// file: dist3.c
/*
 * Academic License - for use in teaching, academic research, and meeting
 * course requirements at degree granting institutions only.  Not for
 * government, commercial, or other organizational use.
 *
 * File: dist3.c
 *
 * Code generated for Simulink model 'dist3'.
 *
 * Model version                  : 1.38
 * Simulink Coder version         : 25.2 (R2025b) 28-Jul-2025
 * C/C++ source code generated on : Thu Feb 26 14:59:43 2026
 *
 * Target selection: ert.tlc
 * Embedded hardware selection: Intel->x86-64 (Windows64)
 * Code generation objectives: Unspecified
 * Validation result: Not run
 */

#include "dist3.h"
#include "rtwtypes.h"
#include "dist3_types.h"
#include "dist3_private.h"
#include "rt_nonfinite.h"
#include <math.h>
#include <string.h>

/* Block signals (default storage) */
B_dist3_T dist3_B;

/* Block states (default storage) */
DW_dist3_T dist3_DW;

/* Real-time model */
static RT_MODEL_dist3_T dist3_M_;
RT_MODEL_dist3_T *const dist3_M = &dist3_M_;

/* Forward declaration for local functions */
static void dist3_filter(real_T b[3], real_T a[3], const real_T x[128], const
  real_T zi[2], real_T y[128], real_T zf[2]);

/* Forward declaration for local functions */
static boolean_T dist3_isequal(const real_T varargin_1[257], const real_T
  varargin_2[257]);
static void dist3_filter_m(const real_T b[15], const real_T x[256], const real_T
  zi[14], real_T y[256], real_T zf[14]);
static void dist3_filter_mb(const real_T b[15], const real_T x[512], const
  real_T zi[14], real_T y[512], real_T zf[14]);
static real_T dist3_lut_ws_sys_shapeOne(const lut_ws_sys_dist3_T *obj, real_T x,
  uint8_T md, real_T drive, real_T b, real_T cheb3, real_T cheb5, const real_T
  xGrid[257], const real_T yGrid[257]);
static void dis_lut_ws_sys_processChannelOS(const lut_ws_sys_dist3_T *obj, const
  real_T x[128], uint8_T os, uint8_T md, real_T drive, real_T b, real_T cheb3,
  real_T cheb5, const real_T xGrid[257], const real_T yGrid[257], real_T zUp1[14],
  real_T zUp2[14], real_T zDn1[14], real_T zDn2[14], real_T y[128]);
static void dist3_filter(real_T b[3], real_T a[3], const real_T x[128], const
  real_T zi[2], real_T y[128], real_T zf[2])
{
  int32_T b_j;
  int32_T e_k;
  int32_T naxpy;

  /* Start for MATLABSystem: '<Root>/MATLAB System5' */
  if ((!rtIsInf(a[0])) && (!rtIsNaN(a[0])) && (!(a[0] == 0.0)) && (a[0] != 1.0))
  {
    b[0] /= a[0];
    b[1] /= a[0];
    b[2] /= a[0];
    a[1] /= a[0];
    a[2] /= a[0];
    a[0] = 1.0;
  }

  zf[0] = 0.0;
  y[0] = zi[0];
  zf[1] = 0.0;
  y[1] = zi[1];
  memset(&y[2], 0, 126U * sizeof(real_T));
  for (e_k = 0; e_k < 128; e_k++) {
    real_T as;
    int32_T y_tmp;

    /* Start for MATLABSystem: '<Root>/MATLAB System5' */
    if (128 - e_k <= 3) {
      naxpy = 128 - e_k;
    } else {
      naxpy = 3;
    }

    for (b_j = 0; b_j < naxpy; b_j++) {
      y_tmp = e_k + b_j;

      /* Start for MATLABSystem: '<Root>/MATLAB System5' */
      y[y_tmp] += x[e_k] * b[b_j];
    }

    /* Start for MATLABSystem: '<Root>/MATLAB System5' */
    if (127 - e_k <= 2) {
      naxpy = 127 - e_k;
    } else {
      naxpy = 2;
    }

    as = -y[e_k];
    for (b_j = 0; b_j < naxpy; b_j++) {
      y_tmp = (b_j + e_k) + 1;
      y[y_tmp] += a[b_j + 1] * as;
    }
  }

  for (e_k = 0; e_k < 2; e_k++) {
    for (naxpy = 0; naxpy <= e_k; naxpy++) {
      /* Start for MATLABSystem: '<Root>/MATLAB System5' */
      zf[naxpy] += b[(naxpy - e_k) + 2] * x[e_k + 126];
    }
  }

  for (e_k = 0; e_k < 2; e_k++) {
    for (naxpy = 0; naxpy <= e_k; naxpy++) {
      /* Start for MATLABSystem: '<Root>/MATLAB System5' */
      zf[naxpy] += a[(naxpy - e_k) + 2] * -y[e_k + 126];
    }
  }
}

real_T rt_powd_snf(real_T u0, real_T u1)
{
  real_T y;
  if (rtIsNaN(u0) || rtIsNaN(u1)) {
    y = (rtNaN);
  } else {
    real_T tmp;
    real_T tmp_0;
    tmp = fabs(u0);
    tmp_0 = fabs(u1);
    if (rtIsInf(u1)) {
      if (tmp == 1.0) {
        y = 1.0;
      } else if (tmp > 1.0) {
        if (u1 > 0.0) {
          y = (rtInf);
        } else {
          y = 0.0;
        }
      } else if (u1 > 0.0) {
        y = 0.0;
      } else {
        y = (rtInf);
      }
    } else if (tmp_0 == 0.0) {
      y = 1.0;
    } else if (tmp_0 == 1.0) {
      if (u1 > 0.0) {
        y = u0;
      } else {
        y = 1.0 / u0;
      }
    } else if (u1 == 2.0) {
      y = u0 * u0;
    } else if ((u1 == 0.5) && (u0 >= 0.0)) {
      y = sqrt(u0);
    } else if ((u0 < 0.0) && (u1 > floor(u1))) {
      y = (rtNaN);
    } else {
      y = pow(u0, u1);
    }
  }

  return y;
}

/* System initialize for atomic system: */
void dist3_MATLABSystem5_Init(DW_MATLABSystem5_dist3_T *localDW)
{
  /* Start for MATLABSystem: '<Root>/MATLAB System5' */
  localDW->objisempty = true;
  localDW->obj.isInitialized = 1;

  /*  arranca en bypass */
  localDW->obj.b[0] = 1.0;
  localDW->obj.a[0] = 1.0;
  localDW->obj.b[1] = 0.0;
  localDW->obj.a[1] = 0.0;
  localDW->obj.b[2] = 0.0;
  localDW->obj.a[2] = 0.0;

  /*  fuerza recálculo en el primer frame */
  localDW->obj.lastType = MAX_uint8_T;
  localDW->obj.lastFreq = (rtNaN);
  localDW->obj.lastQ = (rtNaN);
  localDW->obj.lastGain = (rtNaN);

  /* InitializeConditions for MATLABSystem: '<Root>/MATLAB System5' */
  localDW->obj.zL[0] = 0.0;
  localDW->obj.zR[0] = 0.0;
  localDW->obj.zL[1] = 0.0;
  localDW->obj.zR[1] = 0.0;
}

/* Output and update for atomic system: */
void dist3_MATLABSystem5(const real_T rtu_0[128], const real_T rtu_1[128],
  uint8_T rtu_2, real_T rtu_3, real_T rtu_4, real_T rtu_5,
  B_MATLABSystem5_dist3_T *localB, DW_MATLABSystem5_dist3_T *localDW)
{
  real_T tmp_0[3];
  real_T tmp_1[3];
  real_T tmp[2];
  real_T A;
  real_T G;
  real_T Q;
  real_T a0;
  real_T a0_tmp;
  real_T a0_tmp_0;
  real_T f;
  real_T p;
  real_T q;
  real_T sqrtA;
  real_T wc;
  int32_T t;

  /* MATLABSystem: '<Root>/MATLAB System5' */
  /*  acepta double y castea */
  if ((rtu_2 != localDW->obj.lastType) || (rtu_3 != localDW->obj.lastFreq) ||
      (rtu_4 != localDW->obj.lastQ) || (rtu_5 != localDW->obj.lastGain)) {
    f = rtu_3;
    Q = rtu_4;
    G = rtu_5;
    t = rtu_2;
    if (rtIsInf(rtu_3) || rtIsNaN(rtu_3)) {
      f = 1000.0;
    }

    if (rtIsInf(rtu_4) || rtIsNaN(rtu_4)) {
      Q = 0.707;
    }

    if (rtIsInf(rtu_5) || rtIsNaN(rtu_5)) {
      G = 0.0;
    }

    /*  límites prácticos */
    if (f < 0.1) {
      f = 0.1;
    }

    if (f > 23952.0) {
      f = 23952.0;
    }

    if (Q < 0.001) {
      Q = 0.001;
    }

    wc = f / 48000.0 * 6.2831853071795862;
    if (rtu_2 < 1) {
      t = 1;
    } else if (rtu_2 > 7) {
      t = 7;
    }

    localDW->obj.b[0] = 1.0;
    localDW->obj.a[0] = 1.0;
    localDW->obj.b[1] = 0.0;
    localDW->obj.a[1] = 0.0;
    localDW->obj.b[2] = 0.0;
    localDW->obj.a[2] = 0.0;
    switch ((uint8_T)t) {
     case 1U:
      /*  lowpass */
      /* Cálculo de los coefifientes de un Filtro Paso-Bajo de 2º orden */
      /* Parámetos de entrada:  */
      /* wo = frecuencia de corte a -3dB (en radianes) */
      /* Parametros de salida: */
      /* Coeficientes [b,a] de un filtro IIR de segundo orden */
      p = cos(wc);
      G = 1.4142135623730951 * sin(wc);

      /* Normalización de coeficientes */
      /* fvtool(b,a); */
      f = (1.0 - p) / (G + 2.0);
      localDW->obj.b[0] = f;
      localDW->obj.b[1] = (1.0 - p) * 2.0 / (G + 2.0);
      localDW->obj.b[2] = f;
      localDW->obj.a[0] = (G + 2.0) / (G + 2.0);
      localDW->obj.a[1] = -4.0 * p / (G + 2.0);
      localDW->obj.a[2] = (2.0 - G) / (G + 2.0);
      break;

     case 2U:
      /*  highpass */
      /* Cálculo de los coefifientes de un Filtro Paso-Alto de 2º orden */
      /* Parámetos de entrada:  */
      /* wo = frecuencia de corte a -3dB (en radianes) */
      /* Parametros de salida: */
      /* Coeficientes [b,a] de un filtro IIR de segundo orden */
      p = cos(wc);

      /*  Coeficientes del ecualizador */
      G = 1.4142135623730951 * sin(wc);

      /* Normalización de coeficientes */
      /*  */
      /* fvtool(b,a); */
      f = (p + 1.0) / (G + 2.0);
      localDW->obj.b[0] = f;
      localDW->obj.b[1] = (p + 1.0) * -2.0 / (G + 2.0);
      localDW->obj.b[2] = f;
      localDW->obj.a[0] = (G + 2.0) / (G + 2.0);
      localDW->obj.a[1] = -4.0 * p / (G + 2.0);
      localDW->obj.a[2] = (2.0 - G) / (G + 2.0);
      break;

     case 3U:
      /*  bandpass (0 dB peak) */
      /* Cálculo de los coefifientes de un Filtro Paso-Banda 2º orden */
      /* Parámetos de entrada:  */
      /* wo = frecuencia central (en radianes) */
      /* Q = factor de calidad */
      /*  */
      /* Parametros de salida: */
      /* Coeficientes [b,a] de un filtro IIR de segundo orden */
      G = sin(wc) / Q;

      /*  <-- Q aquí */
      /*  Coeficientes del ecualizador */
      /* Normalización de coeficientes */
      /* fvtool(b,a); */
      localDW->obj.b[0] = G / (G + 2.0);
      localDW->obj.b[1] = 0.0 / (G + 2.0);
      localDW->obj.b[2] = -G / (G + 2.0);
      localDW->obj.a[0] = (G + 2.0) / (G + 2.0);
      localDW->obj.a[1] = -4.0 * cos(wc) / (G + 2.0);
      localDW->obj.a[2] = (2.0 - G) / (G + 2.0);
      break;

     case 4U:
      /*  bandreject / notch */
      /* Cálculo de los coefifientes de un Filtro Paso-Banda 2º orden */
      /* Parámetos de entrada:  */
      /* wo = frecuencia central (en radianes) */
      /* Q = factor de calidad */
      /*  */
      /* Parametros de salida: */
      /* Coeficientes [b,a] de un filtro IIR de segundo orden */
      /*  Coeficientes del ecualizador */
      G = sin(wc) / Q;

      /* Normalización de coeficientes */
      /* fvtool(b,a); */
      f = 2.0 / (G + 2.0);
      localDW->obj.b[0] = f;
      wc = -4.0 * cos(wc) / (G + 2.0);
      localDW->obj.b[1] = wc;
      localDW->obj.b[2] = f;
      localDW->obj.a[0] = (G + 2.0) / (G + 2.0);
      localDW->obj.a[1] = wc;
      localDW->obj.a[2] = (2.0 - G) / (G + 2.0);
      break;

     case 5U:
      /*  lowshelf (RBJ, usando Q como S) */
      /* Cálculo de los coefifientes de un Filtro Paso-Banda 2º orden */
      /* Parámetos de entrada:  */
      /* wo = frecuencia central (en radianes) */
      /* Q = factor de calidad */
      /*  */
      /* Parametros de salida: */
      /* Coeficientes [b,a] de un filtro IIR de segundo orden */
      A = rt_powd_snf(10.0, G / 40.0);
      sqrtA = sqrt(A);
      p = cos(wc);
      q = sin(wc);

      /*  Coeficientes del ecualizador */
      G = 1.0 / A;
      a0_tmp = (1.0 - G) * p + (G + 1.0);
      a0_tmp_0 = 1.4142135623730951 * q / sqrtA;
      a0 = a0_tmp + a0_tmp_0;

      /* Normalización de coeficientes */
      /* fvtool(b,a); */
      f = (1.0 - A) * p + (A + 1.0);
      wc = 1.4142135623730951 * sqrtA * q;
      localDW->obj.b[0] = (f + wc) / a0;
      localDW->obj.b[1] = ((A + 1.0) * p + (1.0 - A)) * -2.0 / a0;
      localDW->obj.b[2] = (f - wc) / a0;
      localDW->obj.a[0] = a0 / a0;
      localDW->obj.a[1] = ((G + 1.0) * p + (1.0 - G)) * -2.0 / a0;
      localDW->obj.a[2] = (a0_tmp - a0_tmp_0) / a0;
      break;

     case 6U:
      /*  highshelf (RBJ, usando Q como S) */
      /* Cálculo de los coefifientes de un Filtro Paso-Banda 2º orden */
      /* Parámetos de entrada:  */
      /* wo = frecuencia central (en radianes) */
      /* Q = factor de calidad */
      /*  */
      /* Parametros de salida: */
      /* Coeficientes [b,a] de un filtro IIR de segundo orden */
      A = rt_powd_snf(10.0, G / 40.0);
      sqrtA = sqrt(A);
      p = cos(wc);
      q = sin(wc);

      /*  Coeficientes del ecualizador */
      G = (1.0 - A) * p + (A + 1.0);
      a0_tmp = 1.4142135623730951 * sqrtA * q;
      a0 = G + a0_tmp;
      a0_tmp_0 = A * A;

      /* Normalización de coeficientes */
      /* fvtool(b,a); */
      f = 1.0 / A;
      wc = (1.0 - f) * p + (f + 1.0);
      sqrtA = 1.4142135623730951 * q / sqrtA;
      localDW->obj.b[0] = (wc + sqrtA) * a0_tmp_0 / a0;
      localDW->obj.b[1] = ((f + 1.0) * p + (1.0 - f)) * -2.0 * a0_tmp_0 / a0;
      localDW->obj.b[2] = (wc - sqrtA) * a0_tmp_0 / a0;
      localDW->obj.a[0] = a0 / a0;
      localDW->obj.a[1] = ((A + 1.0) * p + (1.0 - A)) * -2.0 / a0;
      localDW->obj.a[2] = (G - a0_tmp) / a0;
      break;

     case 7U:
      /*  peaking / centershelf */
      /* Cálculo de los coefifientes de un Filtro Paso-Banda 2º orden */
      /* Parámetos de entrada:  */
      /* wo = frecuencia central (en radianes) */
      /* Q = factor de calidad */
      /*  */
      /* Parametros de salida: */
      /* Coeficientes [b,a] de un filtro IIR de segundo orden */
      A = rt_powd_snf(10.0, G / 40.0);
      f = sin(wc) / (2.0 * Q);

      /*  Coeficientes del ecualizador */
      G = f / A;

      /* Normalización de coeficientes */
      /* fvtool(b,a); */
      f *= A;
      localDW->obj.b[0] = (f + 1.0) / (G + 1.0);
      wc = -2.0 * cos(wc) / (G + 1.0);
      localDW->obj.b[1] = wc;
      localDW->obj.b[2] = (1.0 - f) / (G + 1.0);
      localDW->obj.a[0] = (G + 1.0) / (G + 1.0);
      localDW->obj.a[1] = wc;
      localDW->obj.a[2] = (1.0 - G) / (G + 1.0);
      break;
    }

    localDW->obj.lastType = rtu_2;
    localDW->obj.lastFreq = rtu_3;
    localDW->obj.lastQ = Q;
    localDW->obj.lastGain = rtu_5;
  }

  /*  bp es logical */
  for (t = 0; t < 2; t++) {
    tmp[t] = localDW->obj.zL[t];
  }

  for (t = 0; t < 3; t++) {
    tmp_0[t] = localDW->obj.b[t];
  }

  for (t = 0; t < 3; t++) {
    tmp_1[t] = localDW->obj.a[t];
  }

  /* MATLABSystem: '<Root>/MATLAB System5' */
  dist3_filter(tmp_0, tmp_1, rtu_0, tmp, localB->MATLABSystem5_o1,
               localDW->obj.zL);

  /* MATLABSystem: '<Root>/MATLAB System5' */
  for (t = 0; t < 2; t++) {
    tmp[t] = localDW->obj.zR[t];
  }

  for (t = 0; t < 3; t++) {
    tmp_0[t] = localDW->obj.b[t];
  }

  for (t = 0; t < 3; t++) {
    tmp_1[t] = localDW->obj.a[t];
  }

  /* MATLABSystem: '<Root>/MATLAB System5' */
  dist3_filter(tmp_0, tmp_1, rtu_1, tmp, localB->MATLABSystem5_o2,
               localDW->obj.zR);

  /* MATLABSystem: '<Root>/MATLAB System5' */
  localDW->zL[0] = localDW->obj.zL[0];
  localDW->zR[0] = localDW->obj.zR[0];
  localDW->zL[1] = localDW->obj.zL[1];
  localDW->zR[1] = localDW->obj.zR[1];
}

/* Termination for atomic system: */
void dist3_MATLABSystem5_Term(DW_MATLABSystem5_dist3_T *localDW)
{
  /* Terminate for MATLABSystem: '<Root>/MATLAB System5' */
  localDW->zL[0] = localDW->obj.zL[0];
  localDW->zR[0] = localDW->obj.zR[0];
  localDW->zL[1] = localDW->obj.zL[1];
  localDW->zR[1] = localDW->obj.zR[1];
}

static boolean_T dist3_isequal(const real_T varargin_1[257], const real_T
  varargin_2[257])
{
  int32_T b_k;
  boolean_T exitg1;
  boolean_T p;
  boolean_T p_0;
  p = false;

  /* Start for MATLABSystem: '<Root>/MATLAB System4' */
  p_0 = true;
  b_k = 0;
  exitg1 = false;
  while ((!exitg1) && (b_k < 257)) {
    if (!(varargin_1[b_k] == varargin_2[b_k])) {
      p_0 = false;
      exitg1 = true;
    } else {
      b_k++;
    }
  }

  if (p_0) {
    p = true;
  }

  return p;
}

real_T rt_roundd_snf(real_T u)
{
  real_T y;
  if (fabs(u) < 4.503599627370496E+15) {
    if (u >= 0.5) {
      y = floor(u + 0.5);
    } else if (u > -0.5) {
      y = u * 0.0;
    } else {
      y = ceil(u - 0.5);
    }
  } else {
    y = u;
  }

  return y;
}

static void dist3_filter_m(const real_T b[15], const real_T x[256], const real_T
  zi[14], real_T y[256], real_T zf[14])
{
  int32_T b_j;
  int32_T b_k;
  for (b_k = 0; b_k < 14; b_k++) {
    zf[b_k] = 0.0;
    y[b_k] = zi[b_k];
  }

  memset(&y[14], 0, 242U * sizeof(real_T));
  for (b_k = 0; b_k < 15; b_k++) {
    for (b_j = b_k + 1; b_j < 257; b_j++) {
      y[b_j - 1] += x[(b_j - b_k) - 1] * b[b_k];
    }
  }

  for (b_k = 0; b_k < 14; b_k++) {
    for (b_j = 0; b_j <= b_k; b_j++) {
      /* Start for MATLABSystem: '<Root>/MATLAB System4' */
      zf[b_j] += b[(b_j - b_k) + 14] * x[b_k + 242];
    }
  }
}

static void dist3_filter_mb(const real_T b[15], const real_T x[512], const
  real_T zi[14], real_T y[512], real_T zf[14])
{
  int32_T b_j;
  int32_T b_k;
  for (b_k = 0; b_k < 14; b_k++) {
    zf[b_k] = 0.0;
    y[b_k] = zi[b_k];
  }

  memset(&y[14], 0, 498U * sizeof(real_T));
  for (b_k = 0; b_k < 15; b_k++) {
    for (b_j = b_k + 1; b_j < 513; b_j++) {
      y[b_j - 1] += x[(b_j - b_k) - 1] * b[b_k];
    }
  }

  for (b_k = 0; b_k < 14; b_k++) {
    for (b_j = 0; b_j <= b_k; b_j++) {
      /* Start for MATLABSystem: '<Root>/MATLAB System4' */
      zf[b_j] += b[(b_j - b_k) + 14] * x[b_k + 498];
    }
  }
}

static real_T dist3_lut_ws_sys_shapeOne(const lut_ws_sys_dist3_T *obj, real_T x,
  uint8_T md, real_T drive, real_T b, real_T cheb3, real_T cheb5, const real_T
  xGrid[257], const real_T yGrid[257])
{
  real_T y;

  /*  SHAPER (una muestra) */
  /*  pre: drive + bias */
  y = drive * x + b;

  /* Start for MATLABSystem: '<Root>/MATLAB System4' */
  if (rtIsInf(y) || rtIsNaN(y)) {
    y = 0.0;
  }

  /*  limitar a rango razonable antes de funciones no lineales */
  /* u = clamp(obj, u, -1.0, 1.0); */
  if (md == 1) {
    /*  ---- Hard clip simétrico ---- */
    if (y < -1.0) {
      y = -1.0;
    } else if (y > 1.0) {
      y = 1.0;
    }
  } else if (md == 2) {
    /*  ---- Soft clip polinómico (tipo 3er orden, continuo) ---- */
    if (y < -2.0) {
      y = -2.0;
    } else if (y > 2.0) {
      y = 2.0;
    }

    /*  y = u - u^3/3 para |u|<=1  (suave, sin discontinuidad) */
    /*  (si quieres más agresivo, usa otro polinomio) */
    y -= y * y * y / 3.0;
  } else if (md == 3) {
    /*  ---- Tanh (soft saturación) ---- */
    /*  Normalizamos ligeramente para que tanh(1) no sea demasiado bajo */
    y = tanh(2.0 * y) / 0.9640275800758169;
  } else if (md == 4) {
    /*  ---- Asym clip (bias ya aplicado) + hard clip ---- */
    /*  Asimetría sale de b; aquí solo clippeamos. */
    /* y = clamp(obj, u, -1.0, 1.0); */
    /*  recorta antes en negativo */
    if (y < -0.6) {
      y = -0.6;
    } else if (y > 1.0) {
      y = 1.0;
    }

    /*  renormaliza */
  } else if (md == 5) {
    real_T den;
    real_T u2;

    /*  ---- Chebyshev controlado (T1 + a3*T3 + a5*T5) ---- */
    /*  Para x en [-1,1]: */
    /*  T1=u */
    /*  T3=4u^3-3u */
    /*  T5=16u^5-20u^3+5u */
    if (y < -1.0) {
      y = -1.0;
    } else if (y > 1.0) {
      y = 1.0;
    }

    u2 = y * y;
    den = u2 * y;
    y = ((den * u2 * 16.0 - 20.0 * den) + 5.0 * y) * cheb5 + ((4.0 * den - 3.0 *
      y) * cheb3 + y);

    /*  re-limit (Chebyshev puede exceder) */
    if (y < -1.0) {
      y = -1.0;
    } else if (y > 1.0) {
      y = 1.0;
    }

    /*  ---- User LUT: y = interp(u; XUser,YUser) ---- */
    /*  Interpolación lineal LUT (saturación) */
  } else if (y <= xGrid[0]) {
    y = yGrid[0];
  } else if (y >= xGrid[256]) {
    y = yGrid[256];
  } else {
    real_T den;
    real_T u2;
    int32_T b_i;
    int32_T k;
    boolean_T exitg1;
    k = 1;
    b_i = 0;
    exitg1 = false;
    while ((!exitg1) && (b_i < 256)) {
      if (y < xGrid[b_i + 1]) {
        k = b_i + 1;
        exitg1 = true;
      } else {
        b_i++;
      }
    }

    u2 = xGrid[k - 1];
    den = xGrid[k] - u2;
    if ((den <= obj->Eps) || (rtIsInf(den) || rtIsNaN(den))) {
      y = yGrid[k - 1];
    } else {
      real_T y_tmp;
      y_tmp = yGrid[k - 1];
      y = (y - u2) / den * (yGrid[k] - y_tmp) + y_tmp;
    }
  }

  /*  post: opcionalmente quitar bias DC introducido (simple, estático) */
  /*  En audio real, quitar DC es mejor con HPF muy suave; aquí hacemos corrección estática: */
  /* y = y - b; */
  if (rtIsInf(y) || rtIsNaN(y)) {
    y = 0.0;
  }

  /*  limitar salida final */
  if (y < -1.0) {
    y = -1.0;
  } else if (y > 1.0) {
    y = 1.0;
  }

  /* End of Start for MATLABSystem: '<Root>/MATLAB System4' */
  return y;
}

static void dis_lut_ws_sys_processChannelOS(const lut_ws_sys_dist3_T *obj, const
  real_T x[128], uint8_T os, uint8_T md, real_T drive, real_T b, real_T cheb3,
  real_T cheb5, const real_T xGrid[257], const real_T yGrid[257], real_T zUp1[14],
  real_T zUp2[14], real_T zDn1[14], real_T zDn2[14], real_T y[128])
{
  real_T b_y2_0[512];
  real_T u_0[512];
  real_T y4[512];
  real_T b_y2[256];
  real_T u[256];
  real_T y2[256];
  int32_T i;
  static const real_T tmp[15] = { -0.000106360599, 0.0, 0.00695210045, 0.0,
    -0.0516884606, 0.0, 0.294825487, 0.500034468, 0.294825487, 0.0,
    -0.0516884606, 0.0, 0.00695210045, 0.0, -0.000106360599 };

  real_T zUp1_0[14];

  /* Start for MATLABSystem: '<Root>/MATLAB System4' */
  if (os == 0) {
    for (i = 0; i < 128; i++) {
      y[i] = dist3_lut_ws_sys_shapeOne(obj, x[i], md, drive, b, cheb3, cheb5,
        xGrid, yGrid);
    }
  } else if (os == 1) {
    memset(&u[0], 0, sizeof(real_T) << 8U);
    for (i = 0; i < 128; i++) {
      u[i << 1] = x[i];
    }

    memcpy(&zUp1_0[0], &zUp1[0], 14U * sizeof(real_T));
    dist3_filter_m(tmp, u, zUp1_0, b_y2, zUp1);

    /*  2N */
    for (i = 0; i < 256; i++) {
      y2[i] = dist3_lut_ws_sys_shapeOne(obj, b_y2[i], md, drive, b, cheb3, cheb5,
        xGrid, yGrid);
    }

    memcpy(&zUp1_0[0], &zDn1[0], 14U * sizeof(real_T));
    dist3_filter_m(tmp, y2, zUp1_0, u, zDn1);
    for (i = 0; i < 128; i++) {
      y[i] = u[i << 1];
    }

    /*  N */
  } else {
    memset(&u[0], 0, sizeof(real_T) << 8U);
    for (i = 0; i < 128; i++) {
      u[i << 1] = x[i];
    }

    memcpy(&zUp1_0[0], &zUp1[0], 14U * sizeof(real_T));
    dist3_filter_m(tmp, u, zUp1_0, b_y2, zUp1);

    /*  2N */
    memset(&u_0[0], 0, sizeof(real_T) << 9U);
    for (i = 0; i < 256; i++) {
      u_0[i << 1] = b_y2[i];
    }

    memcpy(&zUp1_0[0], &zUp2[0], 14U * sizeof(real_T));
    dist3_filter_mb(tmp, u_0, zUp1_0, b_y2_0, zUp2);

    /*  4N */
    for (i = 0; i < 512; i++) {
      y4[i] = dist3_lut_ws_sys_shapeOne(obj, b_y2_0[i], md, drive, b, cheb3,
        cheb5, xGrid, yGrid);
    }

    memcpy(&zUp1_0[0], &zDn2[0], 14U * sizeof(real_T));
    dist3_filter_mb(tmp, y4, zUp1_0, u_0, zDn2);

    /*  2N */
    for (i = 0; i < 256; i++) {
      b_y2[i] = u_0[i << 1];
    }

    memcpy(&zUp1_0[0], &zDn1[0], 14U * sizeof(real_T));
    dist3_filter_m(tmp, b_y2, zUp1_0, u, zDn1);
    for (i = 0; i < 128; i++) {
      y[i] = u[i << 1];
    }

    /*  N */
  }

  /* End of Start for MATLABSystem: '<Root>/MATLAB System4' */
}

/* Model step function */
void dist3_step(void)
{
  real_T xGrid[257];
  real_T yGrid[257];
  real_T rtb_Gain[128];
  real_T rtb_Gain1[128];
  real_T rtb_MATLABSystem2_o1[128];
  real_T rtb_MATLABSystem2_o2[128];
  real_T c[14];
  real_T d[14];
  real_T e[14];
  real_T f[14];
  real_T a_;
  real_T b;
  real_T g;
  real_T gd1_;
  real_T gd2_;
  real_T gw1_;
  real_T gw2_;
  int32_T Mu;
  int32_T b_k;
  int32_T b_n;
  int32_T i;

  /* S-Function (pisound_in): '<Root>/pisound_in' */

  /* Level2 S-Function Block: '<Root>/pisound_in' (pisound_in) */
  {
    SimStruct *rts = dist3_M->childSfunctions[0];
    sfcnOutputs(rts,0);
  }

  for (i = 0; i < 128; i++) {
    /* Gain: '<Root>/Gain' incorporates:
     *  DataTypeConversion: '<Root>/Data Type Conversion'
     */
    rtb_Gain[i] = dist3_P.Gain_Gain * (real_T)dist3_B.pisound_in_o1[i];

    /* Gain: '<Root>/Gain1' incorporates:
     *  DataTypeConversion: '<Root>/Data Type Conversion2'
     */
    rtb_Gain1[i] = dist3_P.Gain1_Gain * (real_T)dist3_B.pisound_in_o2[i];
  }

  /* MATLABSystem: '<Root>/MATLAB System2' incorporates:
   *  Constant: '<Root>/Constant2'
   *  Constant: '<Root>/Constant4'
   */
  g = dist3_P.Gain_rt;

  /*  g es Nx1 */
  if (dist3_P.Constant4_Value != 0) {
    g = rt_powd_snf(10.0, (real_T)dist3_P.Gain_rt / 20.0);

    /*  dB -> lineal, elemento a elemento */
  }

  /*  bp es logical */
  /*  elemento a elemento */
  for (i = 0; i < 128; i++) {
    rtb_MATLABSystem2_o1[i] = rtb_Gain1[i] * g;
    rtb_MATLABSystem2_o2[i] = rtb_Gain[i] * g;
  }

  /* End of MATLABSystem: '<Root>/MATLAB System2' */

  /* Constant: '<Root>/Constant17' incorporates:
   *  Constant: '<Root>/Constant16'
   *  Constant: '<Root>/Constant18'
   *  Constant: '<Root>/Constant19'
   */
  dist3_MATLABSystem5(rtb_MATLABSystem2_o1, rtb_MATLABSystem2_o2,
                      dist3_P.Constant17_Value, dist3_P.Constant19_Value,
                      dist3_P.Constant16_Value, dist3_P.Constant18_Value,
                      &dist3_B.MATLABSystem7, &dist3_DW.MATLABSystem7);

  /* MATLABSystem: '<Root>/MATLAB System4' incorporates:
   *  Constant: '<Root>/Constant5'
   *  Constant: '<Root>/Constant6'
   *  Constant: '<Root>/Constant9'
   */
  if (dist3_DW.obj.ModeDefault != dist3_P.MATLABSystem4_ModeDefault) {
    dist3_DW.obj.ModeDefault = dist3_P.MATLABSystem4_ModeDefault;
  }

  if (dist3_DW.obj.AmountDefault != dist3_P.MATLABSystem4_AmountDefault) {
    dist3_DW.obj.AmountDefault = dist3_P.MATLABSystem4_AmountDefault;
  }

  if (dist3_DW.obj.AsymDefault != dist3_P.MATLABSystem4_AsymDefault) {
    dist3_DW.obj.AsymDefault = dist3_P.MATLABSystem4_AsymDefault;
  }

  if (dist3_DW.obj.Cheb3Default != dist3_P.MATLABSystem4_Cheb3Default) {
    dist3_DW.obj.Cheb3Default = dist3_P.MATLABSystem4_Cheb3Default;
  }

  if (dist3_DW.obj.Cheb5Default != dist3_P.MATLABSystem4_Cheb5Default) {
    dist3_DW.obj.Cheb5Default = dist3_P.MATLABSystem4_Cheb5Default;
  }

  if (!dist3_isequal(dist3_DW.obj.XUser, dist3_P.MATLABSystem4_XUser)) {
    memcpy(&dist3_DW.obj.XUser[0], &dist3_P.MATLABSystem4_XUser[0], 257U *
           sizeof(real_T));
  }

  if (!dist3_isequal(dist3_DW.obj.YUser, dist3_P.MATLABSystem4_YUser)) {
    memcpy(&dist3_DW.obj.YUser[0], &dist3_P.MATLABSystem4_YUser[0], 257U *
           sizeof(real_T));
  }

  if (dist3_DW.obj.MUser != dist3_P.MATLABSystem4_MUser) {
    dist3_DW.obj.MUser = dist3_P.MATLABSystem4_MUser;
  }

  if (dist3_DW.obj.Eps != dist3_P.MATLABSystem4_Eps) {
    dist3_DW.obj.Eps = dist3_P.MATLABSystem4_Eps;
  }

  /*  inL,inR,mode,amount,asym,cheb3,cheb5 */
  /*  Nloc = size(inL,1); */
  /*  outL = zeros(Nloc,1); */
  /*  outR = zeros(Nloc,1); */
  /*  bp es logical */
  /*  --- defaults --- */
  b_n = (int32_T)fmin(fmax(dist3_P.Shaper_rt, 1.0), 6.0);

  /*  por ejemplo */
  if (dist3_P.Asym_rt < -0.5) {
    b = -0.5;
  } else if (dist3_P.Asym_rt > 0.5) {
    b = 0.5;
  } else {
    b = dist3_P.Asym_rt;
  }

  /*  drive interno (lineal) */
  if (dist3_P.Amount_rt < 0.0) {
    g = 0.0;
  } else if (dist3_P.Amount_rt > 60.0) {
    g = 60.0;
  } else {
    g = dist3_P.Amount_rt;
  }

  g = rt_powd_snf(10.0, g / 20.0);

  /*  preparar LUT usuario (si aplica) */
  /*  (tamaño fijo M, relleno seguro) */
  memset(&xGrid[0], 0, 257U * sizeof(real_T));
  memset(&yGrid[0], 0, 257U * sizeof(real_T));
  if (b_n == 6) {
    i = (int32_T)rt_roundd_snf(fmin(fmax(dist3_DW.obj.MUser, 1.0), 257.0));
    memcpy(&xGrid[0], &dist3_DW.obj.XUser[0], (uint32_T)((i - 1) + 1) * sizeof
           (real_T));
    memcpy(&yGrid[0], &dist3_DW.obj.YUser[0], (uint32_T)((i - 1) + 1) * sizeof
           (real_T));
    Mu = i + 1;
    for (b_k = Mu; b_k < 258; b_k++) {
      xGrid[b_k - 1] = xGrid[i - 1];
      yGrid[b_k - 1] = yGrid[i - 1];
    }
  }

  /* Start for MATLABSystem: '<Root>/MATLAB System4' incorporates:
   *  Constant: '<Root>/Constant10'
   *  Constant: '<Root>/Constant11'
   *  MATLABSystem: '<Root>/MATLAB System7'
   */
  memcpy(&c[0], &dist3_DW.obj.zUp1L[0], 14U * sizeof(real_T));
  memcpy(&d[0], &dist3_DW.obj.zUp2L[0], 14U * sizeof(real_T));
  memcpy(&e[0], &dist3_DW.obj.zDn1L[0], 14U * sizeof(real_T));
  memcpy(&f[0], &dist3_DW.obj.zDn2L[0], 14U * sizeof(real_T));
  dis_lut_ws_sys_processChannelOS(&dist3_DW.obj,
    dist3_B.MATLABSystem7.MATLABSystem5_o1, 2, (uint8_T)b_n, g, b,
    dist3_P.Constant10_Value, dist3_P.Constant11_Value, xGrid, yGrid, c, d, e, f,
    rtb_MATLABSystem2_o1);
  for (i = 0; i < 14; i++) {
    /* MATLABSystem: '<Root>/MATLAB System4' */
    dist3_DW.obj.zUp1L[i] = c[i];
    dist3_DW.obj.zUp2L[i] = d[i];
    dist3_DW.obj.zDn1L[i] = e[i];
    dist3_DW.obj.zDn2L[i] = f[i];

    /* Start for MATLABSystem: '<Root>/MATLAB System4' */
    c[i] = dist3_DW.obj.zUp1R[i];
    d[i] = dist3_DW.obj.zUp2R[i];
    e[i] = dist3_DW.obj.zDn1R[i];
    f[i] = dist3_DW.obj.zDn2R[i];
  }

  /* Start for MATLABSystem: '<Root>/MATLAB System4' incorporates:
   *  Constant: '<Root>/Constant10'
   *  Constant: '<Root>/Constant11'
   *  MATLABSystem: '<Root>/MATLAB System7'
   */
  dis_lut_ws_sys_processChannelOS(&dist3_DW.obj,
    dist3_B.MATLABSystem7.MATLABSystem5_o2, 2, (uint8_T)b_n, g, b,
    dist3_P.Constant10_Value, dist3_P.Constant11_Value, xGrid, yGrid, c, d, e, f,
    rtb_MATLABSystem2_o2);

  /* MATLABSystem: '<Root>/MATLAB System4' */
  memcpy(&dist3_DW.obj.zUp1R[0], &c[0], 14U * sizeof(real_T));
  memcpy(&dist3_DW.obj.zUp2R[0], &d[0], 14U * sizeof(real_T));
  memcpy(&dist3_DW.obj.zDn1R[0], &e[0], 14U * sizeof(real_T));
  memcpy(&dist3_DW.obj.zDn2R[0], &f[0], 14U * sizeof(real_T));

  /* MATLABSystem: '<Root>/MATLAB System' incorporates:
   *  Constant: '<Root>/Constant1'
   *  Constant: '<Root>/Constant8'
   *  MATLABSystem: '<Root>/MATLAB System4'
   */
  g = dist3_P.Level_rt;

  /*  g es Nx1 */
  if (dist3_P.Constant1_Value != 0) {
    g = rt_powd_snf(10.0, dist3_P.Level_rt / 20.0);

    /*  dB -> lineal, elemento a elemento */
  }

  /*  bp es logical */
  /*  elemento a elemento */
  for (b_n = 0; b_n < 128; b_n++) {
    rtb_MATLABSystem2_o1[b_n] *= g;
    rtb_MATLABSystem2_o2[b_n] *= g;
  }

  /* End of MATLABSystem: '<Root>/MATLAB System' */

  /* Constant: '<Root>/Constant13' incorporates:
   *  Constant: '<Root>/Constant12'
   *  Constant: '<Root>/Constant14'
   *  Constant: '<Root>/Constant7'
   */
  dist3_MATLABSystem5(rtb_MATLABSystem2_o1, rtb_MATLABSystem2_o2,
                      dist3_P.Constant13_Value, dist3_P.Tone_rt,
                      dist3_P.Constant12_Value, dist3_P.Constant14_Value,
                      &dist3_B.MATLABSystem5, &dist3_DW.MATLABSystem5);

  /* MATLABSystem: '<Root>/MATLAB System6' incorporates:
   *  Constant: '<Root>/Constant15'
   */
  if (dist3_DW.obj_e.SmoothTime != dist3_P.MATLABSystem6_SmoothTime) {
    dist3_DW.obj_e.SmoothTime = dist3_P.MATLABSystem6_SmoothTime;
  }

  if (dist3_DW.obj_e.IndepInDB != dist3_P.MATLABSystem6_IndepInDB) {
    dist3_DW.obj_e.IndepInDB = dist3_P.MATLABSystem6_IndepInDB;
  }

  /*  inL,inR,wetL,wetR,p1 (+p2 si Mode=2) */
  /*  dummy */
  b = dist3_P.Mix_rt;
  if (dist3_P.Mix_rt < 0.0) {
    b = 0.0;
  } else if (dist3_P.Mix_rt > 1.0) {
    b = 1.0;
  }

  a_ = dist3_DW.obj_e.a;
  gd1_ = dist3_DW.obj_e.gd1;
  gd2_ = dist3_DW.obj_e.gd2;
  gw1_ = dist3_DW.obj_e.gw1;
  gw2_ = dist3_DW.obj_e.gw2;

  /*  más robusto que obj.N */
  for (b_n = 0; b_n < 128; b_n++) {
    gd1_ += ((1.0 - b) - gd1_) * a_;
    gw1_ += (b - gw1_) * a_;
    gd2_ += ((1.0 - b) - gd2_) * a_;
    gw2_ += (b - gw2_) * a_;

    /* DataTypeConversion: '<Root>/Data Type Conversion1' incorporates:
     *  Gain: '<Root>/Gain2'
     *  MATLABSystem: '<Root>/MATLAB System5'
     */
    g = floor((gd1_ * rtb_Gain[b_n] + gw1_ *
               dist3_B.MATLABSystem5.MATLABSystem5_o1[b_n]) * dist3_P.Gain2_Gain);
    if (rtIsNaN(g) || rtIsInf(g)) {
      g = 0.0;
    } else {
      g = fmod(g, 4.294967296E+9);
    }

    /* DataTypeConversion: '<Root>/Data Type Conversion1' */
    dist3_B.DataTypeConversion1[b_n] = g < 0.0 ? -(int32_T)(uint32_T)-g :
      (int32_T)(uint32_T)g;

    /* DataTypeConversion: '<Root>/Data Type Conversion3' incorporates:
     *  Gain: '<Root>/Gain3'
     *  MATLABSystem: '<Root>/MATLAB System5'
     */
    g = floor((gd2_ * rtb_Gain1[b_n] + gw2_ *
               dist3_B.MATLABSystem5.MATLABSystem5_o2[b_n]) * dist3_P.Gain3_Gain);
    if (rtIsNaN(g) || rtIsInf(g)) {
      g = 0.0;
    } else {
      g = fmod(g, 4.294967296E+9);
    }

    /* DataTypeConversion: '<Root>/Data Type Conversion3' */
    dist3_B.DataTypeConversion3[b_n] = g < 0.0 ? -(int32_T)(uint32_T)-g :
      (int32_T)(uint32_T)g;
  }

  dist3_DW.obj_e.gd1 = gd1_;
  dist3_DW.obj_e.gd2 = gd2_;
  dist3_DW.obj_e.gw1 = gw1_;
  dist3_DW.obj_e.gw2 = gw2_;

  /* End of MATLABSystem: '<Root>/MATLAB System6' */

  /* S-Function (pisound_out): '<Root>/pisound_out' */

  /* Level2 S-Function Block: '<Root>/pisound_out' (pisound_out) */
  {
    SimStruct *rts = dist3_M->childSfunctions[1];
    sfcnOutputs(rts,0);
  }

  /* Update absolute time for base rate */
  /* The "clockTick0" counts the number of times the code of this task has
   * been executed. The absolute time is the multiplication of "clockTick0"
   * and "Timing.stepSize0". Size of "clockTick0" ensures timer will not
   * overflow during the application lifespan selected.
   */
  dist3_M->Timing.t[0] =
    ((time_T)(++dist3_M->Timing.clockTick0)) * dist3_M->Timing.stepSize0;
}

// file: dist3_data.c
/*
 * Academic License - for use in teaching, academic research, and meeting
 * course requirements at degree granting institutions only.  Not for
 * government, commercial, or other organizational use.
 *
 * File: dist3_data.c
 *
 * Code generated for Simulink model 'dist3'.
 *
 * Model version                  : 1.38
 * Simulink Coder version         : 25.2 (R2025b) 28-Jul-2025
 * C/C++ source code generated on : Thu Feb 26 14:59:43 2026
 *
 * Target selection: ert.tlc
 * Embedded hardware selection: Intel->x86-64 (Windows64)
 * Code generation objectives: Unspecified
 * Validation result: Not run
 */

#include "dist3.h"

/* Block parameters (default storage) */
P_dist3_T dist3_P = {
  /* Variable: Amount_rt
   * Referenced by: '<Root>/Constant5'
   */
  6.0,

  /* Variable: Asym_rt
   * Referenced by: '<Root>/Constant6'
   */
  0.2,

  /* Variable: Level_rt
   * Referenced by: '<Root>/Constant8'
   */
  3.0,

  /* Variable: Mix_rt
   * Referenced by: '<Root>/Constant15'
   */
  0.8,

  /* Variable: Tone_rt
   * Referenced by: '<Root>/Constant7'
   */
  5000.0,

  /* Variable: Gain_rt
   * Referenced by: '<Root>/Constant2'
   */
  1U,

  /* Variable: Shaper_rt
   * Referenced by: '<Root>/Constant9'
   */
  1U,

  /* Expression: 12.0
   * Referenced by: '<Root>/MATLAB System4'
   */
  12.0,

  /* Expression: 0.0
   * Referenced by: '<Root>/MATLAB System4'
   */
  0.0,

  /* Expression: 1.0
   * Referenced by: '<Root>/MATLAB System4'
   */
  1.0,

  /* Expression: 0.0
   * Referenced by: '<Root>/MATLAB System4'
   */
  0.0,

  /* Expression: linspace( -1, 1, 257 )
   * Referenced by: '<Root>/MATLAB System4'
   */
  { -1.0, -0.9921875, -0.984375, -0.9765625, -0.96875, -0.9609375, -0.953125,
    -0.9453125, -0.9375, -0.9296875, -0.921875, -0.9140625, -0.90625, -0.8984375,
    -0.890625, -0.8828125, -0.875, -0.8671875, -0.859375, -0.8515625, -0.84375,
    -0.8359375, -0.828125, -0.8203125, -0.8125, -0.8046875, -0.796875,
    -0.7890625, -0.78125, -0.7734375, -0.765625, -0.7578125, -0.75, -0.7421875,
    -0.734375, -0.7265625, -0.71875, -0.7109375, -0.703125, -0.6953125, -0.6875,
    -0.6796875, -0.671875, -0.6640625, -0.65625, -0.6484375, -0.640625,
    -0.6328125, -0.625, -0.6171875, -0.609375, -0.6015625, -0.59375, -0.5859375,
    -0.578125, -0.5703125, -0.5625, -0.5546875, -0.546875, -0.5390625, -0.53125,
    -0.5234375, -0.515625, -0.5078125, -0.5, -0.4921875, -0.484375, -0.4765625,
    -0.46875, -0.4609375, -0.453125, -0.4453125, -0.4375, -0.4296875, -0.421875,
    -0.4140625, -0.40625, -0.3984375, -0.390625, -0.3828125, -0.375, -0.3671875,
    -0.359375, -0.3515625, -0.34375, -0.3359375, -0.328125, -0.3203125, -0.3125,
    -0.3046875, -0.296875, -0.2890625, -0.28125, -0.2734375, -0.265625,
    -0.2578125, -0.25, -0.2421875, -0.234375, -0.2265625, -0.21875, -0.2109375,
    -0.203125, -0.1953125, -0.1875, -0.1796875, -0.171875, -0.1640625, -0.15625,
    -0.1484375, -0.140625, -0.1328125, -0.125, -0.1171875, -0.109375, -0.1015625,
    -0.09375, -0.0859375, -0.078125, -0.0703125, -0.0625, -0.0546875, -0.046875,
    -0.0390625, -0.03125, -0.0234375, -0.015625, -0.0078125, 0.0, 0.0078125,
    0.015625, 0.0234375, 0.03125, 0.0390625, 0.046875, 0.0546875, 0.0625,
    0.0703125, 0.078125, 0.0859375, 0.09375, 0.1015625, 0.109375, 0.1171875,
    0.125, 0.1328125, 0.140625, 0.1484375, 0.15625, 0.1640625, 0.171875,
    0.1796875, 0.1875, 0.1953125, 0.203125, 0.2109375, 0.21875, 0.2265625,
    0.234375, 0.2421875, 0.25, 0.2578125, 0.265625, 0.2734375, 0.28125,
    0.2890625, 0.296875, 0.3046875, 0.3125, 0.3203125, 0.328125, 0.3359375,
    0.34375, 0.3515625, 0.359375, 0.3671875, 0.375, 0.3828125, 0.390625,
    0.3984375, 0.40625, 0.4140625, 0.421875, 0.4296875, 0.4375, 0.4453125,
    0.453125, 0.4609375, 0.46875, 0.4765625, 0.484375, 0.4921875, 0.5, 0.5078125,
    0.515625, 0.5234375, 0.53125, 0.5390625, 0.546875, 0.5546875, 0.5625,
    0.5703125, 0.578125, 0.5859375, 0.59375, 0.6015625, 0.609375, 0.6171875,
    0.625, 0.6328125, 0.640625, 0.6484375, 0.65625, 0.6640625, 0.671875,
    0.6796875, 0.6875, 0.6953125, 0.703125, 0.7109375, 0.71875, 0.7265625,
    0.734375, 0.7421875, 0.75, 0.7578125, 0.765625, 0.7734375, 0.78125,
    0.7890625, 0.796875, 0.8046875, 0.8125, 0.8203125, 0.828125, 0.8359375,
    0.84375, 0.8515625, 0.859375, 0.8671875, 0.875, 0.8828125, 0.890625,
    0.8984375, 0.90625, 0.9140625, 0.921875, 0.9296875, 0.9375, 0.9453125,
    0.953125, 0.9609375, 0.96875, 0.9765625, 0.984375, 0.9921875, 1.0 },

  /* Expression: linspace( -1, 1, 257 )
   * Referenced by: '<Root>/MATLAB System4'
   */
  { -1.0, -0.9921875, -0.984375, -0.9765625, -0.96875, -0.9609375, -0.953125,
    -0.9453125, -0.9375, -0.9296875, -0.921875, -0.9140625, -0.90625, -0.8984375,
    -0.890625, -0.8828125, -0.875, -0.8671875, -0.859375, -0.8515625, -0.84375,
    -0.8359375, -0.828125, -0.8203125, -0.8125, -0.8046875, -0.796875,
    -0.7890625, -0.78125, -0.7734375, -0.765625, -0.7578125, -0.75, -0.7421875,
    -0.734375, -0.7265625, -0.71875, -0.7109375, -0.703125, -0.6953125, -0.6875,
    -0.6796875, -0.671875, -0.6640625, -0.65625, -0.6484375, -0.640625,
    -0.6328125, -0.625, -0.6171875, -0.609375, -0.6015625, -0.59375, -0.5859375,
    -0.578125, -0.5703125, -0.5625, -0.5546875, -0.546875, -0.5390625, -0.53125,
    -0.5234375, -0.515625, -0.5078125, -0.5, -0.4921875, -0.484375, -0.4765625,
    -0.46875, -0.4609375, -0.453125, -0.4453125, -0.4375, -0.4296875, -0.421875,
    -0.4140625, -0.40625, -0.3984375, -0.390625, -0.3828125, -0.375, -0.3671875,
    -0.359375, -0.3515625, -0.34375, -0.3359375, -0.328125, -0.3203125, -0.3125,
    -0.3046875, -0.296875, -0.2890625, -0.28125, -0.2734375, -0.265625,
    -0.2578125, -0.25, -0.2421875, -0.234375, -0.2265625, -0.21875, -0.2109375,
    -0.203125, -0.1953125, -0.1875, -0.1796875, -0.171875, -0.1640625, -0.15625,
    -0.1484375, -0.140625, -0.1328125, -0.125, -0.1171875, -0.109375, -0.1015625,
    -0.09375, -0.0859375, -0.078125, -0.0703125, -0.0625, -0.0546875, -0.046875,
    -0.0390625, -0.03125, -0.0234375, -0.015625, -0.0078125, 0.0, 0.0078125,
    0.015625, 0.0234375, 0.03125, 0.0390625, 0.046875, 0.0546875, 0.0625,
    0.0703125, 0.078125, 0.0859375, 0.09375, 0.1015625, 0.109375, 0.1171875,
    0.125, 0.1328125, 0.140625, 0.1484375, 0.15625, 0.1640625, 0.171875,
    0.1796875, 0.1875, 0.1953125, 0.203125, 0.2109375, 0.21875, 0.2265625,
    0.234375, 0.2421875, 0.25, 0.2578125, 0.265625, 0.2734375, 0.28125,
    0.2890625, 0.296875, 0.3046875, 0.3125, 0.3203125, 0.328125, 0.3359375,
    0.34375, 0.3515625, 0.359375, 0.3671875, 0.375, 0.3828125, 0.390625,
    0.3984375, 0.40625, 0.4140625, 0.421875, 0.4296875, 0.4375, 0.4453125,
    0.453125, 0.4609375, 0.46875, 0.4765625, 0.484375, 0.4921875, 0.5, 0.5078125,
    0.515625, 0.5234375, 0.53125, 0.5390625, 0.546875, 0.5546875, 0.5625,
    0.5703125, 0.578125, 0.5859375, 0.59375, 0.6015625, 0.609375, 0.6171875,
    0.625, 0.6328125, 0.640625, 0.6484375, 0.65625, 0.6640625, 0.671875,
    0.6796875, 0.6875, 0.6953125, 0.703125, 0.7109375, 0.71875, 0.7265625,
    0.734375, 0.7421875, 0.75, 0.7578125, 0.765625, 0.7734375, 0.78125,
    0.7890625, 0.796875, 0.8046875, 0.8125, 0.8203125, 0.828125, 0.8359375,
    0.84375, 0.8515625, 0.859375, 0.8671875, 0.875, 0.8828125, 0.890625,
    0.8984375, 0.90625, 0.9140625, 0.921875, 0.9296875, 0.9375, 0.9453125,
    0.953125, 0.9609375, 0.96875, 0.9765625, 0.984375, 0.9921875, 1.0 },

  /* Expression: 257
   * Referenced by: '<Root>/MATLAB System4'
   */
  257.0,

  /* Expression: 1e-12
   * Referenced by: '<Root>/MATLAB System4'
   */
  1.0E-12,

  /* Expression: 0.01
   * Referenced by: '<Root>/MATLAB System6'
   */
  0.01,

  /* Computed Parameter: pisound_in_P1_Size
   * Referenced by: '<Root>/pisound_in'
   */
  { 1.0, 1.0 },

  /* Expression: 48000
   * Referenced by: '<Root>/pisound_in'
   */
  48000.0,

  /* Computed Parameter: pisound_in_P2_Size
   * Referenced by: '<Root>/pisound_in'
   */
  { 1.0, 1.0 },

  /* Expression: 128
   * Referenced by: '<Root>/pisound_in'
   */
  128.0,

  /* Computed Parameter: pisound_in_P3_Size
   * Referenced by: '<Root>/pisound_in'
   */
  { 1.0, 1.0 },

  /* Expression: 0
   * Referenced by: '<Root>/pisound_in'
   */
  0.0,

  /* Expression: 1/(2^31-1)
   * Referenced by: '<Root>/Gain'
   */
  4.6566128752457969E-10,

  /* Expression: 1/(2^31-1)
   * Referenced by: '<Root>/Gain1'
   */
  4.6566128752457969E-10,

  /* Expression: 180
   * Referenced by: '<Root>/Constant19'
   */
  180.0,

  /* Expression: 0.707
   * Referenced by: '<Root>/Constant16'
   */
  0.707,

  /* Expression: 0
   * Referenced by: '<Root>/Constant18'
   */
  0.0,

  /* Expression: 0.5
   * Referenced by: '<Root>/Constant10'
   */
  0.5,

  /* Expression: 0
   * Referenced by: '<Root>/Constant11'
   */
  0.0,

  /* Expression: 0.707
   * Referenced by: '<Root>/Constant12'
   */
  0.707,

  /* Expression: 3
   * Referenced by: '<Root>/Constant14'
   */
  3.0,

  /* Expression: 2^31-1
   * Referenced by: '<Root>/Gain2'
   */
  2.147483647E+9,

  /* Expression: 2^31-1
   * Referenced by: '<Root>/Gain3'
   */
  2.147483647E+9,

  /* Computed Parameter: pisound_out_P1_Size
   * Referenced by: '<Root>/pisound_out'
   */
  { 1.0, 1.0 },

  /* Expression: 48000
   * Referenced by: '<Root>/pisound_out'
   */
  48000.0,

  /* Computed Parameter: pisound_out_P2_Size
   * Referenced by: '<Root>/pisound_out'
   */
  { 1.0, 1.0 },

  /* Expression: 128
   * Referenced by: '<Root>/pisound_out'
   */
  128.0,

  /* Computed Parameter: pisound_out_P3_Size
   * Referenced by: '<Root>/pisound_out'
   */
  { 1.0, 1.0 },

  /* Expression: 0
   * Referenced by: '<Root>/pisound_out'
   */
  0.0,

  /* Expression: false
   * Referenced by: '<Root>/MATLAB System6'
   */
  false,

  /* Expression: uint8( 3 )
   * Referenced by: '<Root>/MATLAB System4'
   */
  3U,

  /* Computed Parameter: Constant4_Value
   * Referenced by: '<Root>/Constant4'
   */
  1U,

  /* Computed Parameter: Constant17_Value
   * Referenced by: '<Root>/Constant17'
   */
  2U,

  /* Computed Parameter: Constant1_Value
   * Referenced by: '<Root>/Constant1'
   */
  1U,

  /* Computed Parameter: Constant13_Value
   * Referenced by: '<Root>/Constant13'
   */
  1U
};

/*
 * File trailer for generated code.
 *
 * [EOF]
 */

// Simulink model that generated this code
simulink model "dist3"  (R2025b)
settings: Solver=FixedStepDiscrete  StartTime=0.0  StopTime=inf  FixedStep=128/48000  RelTol=1e-3
model workspace (MATLAB code in the model file):
  | Gain_rt = Simulink.Parameter(1.0);
  | Bypass_rt = Simulink.Parameter(false);
undefined symbols (not defined in the file): Amount_rt, Asym_rt, Level_rt, Mix_rt, Shaper_rt, Tone_rt

== system dist3 ==
  Constant1 : Constant  OutDataTypeStr=uint8
  Constant10 : Constant  Value=0.5  OutDataTypeStr=double
  Constant11 : Constant  Value=0  OutDataTypeStr=double
  Constant12 : Constant  Value=0.707  OutDataTypeStr=double
  Constant13 : Constant  OutDataTypeStr=uint8
  Constant14 : Constant  Value=3  OutDataTypeStr=double
  Constant15 : Constant  Value=Mix_rt  OutDataTypeStr=double
  Constant16 : Constant  Value=0.707  OutDataTypeStr=double
  Constant17 : Constant  Value=2  OutDataTypeStr=uint8
  Constant18 : Constant  Value=0  OutDataTypeStr=double
  Constant19 : Constant  Value=180  OutDataTypeStr=double
  Constant2 : Constant  Value=Gain_rt  OutDataTypeStr=uint8
  Constant4 : Constant  OutDataTypeStr=uint8
  Constant5 : Constant  Value=Amount_rt  OutDataTypeStr=double
  Constant6 : Constant  Value=Asym_rt  OutDataTypeStr=double
  Constant7 : Constant  Value=Tone_rt  OutDataTypeStr=double
  Constant8 : Constant  Value=Level_rt  OutDataTypeStr=double
  Constant9 : Constant  Value=Shaper_rt  OutDataTypeStr=uint8
  Data Type Conversion : DataTypeConversion  OutDataTypeStr=double  SaturateOnIntegerOverflow=off  RndMeth=Floor
  Data Type Conversion1 : DataTypeConversion  OutDataTypeStr=int32  SaturateOnIntegerOverflow=off  RndMeth=Floor
  Data Type Conversion2 : DataTypeConversion  OutDataTypeStr=double  SaturateOnIntegerOverflow=off  RndMeth=Floor
  Data Type Conversion3 : DataTypeConversion  OutDataTypeStr=int32  SaturateOnIntegerOverflow=off  RndMeth=Floor
  Gain : Gain  Gain=1/(2^31-1)
  Gain1 : Gain  Gain=1/(2^31-1)
  Gain2 : Gain  Gain=2^31-1
  Gain3 : Gain  Gain=2^31-1
  MATLAB System : MATLABSystem  System=vca_sys  N=128  Fs=48000  bypass=uint8(0)  SimulateUsing=Code generation
  MATLAB System2 : MATLABSystem  System=vca_sys  N=128  Fs=48000  bypass=uint8(0)  SimulateUsing=Code generation
  MATLAB System4 : MATLABSystem  System=lut_ws_sys  N=128  M=257  bypass=uint8(0)  OS=uint8(2)  HB15=[ -1.06360599e-04, 0, 6.95210045e-03, 0, -5.16884606e-02, 0, 2.94825487e-01, 5.00034468e-01, 2.94825487e-01, 0, -5.16884606e-02, 0, 6.95210045e-03, 0, -1.06360599e-04 ]  ModeDefault=uint8( 3 )  AmountDefault=12.0  AsymDefault=0.0  Cheb3Default=1.0  Cheb5Default=0.0  XUser=linspace( -1, 1, 257 )  YUser=linspace( -1, 1, 257 )  MUser=257  Eps=1e-12  SimulateUsing=Code generation
  MATLAB System5 : MATLABSystem  System=vcf_sys  N=128  Fs=48000  bypass=uint8(0)  SimulateUsing=Code generation
  MATLAB System6 : MATLABSystem  System=mix_sys  N=128  Fs=48000  Mode=uint8( 0 )  SmoothTime=0.01  IndepInDB=false  SimulateUsing=Code generation
  MATLAB System7 : MATLABSystem  System=vcf_sys  N=128  Fs=48000  bypass=uint8(0)  SimulateUsing=Code generation
  pisound_in : S-Function  FunctionName=pisound_in  Parameters=48000, 128, 0  SFunctionDeploymentMode=off  EnableBusSupport=off
  pisound_out : S-Function  FunctionName=pisound_out  Parameters=48000, 128, 0  SFunctionDeploymentMode=off  EnableBusSupport=off
  wires:
  pisound_in/1 -> Data Type Conversion/1
  pisound_in/2 -> Data Type Conversion2/1
  Data Type Conversion1/1 -> pisound_out/1
  Data Type Conversion3/1 -> pisound_out/2
  Gain2/1 -> Data Type Conversion1/1
  Gain3/1 -> Data Type Conversion3/1
  Data Type Conversion/1 -> Gain/1
  Data Type Conversion2/1 -> Gain1/1
  pisound_in/3 -> pisound_out/3
  pisound_in/4 -> pisound_out/4
  Gain/1 -> MATLAB System2/2, MATLAB System6/1
  Gain1/1 -> MATLAB System6/2, MATLAB System2/1
  Constant1/1 -> MATLAB System/4
  Constant2/1 -> MATLAB System2/3
  MATLAB System4/1 -> MATLAB System/1
  MATLAB System4/2 -> MATLAB System/2
  Constant8/1 -> MATLAB System/3
  Constant9/1 -> MATLAB System4/3
  Constant5/1 -> MATLAB System4/4
  Constant6/1 -> MATLAB System4/5
  Constant7/1 -> MATLAB System5/4
  MATLAB System/1 -> MATLAB System5/1
  MATLAB System/2 -> MATLAB System5/2
  Constant4/1 -> MATLAB System2/4
  Constant10/1 -> MATLAB System4/6
  Constant11/1 -> MATLAB System4/7
  Constant12/1 -> MATLAB System5/5
  Constant13/1 -> MATLAB System5/3
  Constant14/1 -> MATLAB System5/6
  MATLAB System6/1 -> Gain2/1
  MATLAB System6/2 -> Gain3/1
  MATLAB System5/1 -> MATLAB System6/3
  MATLAB System5/2 -> MATLAB System6/4
  Constant15/1 -> MATLAB System6/5
  Constant19/1 -> MATLAB System7/4
  Constant17/1 -> MATLAB System7/3
  Constant16/1 -> MATLAB System7/5
  Constant18/1 -> MATLAB System7/6
  MATLAB System2/1 -> MATLAB System7/1
  MATLAB System2/2 -> MATLAB System7/2
  MATLAB System7/1 -> MATLAB System4/1
  MATLAB System7/2 -> MATLAB System4/2
